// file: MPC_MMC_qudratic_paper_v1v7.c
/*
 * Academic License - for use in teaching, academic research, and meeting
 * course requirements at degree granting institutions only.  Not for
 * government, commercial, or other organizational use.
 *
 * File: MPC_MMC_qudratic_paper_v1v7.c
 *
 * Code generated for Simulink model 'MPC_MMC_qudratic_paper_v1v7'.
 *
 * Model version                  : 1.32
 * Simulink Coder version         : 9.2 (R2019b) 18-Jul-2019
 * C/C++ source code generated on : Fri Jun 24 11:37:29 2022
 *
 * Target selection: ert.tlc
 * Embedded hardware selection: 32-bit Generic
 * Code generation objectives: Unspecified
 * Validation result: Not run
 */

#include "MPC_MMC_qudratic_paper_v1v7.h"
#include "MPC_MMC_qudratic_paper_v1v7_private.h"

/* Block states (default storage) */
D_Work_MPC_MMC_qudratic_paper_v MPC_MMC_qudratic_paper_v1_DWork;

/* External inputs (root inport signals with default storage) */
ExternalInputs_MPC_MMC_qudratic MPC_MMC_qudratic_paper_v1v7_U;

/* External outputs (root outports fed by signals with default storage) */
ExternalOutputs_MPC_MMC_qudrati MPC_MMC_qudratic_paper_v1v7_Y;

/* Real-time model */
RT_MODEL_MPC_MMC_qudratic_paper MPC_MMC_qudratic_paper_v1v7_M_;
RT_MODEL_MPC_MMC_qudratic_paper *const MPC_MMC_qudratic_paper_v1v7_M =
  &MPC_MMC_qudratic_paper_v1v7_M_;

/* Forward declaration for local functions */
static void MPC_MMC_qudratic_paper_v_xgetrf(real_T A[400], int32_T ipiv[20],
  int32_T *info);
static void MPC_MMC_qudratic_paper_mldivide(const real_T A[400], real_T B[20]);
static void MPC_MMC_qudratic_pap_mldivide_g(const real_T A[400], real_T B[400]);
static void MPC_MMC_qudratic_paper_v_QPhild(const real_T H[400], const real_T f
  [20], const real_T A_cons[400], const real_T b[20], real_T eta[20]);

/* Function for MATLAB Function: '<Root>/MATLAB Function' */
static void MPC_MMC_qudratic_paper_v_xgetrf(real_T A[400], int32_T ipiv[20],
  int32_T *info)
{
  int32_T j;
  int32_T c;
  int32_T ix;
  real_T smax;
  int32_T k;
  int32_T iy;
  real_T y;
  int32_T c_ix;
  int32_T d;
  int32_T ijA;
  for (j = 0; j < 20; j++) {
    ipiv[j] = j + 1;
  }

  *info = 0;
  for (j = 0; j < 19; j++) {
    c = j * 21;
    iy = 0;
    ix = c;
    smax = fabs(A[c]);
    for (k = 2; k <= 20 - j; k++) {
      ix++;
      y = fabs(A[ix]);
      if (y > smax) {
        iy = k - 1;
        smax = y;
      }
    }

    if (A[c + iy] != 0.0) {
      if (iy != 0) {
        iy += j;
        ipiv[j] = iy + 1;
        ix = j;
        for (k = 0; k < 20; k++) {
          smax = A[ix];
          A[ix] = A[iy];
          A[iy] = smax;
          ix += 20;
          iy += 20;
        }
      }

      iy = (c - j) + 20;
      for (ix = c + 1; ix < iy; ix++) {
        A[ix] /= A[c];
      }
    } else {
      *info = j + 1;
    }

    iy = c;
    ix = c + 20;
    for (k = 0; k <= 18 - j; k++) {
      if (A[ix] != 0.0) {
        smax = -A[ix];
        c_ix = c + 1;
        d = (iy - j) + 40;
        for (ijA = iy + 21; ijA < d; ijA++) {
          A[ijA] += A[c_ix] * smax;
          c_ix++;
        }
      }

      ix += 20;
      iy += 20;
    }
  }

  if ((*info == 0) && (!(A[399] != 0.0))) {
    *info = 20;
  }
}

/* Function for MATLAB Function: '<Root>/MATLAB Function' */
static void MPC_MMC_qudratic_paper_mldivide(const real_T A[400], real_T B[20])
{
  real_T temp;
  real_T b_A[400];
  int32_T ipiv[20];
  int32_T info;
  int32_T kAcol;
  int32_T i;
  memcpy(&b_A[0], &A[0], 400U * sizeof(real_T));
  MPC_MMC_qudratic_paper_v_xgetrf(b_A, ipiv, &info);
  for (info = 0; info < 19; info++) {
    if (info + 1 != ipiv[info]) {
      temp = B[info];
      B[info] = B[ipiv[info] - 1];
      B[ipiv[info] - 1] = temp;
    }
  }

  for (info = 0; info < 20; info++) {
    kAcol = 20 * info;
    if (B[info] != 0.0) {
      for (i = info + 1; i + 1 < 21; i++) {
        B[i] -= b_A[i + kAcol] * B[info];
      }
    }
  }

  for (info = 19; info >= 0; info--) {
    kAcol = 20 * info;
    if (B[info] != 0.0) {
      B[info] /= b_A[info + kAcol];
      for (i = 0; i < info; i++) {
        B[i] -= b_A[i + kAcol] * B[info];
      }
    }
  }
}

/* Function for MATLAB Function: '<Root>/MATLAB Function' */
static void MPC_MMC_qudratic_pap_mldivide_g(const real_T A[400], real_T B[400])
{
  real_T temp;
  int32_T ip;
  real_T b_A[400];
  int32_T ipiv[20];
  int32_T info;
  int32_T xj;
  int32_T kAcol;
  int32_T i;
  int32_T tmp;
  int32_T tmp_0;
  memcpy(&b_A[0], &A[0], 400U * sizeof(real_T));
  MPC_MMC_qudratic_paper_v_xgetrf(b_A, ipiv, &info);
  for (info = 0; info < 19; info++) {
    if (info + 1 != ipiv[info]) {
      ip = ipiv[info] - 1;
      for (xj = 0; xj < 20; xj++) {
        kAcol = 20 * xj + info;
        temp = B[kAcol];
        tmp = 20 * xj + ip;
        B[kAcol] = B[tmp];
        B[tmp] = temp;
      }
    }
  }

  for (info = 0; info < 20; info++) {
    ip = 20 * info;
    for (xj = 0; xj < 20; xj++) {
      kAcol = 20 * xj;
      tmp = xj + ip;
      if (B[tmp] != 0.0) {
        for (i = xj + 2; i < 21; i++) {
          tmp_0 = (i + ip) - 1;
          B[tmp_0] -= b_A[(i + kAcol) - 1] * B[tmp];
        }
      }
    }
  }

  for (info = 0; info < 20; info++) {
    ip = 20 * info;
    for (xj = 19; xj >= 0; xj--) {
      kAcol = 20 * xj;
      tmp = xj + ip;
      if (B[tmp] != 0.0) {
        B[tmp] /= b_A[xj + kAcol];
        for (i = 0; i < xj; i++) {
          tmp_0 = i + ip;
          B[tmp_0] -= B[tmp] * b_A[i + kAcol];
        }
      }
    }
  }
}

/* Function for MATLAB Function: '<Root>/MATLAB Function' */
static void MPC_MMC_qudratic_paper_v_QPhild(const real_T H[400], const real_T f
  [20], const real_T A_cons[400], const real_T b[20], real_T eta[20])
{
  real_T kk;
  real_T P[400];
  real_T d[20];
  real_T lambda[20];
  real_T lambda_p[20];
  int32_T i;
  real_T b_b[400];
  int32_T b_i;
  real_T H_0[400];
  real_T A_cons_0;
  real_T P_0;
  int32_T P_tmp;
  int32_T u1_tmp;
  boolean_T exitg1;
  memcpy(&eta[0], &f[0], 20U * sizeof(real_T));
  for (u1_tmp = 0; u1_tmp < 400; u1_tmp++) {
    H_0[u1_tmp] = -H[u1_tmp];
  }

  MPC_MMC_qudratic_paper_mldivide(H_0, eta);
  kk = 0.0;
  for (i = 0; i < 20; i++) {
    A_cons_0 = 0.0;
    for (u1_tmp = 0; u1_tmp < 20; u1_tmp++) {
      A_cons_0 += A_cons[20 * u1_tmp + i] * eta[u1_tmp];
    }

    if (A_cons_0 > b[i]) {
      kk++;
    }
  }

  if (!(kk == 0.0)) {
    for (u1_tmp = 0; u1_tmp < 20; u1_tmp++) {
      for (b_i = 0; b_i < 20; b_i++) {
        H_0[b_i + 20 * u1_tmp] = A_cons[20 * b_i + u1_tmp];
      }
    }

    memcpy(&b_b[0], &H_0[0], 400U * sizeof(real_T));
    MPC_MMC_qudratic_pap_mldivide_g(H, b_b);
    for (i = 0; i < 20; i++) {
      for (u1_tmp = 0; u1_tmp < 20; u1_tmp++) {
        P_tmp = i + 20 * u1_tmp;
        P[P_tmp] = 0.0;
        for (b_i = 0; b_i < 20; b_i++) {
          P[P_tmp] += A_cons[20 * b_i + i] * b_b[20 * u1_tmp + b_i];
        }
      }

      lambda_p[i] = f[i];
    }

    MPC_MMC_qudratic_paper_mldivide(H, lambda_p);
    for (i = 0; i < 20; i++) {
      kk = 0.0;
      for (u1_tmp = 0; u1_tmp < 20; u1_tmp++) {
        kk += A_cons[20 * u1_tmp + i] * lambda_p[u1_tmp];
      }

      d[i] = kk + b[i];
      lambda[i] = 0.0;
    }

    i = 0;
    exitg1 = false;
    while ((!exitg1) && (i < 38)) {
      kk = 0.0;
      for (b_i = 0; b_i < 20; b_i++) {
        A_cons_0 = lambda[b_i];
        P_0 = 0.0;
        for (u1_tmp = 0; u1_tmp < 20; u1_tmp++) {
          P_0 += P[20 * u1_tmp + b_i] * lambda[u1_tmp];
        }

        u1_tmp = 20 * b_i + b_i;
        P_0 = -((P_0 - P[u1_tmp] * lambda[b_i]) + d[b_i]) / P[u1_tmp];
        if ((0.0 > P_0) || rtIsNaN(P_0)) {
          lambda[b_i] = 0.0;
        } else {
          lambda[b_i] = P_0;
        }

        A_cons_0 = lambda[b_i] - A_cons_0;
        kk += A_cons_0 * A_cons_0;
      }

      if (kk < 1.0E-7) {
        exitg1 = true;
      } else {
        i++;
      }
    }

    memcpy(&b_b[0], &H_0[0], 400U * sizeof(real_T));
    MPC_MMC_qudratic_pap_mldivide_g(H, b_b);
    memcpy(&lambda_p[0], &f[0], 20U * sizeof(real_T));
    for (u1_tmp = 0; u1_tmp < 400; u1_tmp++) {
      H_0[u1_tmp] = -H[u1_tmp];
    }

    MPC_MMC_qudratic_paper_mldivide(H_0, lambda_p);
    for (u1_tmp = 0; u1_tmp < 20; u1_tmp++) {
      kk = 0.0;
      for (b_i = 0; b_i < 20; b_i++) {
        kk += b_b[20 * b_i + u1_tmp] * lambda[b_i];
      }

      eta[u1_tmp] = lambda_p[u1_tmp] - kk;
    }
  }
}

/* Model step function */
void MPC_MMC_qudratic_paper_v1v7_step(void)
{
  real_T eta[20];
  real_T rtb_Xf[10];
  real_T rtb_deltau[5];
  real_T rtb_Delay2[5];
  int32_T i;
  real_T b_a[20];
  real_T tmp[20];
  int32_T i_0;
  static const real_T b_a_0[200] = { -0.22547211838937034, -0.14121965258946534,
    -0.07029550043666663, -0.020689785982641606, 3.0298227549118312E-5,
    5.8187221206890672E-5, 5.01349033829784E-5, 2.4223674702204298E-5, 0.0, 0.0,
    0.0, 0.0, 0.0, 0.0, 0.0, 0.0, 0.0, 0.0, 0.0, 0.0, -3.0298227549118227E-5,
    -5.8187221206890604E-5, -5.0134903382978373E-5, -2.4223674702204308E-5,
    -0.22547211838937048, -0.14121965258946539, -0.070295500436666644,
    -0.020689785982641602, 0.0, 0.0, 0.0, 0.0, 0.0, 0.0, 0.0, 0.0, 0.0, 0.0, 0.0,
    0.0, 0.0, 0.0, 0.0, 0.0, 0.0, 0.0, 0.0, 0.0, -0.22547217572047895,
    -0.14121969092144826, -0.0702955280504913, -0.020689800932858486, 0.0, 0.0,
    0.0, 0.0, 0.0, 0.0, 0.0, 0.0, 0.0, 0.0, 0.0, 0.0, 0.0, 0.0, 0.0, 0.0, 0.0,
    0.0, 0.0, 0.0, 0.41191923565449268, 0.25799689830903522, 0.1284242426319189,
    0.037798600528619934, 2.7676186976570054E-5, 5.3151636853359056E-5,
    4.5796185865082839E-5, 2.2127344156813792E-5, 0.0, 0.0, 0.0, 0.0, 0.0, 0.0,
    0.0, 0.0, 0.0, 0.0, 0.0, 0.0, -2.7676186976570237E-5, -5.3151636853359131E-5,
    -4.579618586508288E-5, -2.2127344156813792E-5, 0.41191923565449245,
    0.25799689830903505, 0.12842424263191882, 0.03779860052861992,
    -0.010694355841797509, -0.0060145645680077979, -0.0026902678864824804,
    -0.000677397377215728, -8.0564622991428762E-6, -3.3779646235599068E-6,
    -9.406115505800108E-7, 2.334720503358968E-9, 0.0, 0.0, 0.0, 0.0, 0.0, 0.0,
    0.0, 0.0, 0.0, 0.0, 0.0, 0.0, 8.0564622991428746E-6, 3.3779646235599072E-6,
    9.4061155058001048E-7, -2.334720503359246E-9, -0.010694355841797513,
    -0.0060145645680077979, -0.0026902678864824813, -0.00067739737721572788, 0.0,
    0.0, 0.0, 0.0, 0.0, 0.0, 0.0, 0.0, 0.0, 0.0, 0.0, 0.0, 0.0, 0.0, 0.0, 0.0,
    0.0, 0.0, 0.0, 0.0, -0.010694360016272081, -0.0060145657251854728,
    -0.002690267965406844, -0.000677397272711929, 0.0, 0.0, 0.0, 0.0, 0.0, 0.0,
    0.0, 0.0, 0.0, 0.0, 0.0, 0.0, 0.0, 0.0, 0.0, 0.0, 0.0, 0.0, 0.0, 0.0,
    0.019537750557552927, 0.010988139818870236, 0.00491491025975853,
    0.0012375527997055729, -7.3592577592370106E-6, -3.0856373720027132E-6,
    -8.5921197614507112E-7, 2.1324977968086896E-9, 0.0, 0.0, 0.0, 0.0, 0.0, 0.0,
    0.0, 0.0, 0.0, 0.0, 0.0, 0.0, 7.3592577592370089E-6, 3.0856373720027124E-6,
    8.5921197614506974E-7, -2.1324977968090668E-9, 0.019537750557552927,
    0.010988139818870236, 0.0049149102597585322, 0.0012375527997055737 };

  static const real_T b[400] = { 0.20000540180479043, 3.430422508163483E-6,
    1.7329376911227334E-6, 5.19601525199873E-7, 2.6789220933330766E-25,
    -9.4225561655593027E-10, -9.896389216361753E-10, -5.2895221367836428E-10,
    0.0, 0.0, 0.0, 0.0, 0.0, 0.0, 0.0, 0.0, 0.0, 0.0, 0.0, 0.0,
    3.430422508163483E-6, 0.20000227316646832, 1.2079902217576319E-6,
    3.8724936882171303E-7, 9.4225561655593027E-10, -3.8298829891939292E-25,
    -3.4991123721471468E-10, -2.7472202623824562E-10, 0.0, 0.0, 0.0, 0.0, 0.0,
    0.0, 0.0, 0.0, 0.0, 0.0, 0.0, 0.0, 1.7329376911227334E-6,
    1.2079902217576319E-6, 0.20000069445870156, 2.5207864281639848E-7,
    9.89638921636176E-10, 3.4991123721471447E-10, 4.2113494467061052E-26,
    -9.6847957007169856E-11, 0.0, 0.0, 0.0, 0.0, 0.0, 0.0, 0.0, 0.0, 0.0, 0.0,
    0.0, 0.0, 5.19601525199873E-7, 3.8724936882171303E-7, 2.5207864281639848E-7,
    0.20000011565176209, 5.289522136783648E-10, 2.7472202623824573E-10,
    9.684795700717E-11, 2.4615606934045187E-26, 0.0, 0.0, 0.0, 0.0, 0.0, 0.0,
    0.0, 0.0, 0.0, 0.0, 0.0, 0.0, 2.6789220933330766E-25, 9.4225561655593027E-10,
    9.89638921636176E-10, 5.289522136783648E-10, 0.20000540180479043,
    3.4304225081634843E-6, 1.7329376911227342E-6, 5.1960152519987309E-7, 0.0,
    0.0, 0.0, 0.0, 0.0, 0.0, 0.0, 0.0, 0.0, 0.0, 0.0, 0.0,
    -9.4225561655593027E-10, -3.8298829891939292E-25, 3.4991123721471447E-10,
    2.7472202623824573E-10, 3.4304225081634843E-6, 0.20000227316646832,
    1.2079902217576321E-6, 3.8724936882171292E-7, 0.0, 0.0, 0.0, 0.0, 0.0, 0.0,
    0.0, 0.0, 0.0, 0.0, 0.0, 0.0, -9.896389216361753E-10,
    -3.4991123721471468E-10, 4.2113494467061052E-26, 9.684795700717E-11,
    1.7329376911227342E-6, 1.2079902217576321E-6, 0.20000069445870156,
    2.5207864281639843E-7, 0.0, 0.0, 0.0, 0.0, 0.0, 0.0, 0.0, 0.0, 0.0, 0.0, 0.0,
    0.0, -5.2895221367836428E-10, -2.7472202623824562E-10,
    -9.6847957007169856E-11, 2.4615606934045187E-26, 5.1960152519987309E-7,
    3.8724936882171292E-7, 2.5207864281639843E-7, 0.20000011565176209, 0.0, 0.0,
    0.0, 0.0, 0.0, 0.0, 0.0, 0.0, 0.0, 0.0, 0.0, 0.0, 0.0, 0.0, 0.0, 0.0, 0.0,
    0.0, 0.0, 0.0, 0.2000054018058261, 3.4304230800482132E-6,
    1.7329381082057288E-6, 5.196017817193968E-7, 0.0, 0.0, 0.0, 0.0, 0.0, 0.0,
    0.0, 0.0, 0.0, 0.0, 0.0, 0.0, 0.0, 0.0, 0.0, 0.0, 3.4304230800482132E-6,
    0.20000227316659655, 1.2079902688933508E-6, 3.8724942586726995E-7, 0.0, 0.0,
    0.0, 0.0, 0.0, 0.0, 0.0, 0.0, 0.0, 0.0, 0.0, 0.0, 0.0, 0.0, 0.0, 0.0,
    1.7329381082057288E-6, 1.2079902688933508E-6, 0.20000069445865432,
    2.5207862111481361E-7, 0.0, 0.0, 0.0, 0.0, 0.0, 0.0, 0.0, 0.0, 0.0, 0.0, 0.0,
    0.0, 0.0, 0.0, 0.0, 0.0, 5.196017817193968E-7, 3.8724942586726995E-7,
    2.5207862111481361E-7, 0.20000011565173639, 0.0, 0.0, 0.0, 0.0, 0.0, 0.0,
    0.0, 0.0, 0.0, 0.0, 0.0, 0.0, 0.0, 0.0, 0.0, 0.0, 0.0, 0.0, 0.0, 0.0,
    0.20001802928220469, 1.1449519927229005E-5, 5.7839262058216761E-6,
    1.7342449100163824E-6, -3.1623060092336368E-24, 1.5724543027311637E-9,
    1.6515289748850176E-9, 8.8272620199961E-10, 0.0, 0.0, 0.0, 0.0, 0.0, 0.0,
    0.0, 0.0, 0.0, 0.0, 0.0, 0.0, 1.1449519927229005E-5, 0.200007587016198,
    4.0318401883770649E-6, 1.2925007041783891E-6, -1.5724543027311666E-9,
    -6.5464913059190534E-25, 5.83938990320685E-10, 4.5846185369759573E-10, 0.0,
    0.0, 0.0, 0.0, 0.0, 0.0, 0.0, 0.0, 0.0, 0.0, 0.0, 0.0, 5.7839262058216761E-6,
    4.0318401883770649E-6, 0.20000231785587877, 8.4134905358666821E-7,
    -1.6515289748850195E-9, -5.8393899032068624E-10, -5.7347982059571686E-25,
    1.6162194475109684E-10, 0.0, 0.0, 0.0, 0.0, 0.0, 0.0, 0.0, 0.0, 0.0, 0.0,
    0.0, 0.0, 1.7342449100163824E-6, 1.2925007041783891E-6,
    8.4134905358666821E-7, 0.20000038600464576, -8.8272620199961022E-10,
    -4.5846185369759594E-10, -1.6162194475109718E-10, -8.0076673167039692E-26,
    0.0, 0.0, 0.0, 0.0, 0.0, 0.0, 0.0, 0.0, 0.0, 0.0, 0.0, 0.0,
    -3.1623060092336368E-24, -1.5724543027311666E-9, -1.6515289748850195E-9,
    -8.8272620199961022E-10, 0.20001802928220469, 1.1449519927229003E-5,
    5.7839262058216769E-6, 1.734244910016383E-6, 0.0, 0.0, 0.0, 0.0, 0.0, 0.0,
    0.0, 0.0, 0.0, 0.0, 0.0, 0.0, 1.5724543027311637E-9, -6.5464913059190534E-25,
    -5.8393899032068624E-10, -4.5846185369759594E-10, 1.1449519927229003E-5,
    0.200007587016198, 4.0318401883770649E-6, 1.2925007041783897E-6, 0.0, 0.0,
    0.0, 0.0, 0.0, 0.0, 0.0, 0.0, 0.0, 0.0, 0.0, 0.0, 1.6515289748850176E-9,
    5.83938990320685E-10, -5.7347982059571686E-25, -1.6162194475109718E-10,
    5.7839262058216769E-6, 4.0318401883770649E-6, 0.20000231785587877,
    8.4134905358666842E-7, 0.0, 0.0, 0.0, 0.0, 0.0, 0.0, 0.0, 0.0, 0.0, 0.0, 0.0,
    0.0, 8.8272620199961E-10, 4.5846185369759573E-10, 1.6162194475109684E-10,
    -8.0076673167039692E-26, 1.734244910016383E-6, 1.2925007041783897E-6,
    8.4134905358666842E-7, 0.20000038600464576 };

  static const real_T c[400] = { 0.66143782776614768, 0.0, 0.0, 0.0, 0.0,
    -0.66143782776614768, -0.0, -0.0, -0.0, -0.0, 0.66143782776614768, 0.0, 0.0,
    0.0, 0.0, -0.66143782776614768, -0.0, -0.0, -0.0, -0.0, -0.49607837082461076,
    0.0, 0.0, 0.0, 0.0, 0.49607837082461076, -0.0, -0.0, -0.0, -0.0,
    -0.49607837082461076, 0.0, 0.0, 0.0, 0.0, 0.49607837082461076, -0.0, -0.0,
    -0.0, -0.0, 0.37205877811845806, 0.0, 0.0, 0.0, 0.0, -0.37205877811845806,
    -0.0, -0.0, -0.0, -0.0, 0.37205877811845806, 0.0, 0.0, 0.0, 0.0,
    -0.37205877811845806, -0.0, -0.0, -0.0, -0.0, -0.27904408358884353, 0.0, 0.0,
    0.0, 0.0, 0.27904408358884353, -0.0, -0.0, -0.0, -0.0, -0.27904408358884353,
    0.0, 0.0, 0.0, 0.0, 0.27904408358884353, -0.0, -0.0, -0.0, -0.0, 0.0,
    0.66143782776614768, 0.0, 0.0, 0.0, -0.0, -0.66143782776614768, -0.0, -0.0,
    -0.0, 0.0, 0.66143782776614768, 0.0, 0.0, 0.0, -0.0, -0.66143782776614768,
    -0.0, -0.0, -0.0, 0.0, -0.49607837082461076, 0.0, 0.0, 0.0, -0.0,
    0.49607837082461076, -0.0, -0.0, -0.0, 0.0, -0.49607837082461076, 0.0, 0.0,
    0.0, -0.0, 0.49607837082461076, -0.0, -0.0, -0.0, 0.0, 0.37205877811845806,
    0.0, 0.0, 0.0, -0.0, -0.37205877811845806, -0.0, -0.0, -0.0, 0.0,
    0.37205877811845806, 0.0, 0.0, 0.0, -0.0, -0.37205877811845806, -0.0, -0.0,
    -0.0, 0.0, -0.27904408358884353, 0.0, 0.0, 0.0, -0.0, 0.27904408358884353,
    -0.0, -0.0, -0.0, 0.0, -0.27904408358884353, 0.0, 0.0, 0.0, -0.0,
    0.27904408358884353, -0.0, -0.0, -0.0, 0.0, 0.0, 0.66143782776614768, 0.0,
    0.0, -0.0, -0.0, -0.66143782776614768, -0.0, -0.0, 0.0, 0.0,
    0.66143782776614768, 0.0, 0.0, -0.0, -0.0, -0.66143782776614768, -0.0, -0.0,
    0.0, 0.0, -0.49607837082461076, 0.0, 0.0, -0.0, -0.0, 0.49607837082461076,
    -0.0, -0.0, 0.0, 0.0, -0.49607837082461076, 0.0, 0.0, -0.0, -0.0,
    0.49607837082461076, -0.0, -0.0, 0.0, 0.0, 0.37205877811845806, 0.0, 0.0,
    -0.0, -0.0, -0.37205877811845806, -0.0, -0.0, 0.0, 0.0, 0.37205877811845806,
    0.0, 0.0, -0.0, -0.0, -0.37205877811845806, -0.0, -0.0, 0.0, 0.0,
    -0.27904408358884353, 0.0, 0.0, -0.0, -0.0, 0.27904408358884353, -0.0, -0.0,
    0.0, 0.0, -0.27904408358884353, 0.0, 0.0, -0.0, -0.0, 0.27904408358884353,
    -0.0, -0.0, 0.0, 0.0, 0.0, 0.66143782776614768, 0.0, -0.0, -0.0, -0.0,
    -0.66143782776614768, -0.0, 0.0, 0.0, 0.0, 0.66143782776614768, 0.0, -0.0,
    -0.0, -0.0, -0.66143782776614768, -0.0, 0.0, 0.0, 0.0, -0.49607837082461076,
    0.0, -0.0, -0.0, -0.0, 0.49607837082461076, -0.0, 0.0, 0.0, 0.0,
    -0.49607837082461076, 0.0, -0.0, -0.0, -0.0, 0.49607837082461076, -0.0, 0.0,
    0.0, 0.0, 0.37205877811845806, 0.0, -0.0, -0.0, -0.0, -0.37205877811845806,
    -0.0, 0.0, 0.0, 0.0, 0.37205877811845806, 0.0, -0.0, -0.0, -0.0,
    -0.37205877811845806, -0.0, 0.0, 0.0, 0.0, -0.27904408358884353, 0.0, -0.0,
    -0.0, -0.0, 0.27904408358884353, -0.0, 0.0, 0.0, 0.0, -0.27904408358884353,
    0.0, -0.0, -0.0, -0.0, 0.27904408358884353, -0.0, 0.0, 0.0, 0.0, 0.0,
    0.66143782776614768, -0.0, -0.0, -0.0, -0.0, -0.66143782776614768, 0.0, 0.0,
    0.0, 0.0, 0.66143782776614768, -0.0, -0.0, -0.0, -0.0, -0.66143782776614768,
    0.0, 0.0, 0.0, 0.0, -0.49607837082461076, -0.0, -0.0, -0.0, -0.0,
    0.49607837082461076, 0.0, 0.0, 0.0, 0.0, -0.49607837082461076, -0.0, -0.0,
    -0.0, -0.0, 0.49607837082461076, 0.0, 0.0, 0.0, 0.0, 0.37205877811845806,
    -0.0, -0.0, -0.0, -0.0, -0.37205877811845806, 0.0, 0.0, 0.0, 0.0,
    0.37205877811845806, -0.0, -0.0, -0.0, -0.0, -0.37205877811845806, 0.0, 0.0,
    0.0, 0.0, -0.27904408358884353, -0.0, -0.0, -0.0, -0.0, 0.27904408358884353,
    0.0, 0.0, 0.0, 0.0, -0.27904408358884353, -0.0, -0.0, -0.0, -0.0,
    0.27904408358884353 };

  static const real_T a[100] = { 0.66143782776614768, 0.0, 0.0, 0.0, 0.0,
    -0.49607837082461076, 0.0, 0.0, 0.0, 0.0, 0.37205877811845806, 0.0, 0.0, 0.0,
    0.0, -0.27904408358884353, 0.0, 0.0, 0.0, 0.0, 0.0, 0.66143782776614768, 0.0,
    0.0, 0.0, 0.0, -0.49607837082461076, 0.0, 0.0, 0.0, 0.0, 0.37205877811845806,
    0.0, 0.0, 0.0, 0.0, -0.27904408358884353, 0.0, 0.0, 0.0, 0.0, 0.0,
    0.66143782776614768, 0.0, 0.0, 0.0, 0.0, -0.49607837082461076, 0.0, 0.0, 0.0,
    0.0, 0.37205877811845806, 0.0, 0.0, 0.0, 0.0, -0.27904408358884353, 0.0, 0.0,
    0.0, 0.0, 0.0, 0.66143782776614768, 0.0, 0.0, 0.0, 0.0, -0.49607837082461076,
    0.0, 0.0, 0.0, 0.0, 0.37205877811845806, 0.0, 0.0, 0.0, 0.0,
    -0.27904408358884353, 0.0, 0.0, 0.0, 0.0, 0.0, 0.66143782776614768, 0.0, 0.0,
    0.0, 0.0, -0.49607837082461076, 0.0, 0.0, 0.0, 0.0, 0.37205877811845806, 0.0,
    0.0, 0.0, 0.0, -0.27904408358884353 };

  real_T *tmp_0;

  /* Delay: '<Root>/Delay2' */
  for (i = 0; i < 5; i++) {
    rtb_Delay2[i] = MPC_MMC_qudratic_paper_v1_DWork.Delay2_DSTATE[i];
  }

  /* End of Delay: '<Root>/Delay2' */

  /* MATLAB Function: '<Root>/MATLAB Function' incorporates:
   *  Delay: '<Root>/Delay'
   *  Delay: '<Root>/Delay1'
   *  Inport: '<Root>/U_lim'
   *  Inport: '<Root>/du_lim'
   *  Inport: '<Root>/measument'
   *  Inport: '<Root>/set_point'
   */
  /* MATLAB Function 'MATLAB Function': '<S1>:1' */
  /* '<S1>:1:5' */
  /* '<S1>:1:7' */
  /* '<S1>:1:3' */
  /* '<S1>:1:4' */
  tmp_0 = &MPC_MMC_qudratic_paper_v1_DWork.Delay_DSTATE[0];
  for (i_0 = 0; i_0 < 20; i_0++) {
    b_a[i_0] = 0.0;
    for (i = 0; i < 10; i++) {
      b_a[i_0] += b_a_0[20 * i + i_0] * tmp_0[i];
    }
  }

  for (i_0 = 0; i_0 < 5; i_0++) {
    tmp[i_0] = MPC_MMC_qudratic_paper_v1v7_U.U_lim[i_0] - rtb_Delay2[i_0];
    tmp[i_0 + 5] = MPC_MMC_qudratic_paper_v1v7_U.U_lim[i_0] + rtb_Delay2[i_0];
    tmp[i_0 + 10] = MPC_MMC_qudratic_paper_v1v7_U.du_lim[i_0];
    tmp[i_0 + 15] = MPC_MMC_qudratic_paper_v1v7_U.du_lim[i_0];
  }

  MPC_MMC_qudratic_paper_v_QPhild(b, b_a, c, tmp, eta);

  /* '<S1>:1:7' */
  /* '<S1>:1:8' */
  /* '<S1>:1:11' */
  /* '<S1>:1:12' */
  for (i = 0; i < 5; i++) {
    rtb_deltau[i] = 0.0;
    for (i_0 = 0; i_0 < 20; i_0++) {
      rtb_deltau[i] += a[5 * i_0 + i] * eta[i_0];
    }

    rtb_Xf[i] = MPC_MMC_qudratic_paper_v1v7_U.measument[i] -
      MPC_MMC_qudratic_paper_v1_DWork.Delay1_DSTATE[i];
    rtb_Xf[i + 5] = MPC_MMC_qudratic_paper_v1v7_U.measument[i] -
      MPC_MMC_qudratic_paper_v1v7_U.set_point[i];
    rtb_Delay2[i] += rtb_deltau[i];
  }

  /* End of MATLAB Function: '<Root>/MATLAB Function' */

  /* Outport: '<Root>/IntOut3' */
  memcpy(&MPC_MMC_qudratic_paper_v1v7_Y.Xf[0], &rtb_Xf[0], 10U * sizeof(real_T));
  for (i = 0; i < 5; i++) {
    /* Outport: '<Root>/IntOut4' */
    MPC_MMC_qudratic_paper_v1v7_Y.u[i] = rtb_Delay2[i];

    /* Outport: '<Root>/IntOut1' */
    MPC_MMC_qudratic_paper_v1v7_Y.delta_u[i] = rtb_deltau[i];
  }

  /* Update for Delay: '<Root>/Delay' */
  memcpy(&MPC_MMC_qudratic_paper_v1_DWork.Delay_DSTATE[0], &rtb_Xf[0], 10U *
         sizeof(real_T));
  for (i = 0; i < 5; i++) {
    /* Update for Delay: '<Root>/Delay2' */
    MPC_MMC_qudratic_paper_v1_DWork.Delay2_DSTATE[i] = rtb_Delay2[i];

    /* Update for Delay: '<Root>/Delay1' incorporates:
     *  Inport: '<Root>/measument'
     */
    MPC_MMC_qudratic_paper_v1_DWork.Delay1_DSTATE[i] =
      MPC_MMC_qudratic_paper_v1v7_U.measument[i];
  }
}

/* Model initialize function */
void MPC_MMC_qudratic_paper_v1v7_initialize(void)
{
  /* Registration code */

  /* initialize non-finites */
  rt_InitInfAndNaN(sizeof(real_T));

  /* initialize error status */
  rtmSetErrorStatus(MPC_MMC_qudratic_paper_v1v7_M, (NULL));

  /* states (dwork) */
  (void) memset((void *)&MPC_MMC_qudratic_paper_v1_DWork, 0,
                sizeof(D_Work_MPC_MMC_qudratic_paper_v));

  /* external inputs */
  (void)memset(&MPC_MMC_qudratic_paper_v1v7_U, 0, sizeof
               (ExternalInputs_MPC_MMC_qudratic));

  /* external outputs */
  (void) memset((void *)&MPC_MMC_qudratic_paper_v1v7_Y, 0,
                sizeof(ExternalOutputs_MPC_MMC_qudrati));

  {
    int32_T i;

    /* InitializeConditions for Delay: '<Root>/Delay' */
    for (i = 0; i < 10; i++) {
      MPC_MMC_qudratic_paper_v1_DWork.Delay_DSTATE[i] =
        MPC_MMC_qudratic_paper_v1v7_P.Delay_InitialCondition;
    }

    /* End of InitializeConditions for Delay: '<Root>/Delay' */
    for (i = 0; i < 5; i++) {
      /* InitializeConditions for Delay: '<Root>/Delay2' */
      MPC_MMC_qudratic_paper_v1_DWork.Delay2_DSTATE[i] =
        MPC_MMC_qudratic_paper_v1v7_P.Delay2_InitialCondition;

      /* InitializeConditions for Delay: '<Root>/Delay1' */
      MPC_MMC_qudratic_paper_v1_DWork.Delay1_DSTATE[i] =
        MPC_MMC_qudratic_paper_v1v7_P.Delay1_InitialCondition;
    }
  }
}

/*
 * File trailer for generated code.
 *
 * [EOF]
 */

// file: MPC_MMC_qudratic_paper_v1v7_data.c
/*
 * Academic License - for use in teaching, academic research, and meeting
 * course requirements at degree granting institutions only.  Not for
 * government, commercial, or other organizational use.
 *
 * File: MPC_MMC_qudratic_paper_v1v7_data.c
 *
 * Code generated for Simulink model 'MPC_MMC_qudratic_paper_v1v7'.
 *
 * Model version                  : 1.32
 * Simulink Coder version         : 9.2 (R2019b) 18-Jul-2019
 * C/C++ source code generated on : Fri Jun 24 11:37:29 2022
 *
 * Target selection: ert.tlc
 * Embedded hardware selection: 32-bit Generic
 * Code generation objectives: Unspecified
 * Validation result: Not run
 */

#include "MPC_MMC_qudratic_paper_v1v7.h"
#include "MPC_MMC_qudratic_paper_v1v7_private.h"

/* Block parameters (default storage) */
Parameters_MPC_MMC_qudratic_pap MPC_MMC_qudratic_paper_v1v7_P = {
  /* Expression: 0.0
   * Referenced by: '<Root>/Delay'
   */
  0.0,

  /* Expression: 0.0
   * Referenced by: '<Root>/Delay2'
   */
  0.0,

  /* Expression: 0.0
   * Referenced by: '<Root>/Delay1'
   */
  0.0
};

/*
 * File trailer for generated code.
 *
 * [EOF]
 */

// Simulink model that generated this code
simulink model "MPC_MMC_qudratic_paper_v1v7"  (R2019b)
settings: Solver=ode3  StartTime=0.0  StopTime=3  FixedStep=0.000080  RelTol=1e-3  EnableMultiTasking=on

== system MPC_MMC_qudratic_paper_v1v7 ==
  set_point : Inport  PortDimensions=5
  measument : Inport  Port=2  PortDimensions=5
  U_lim : Inport  Port=3  PortDimensions=5
  du_lim : Inport  Port=4  PortDimensions=5
  Delay : Delay  DelayLength=1
  Delay1 : Delay  DelayLength=1
  Delay2 : Delay  DelayLength=1
  MATLAB Function : MATLAB Function  TreatAsAtomicUnit=on
  IntOut3 : Outport  SignalName=Xf
  IntOut4 : Outport  Port=2  SignalName=u
  IntOut1 : Outport  Port=3  SignalName=delta_u
  wires:
  set_point/1 -> MATLAB Function/1(r)
  MATLAB Function/1(Xf) -> Delay/1, IntOut3/1
  measument/1 -> MATLAB Function/2(xm_old), Delay1/1
  MATLAB Function/3(deltau) -> IntOut1/1
  Delay1/1 -> MATLAB Function/5(Xm_k_1)
  Delay/1 -> MATLAB Function/3(Xf_old)
  Delay2/1 -> MATLAB Function/4(u_old)
  MATLAB Function/2(u) -> Delay2/1, IntOut4/1
  U_lim/1 -> MATLAB Function/6(U_lim)
  du_lim/1 -> MATLAB Function/7(du_lim)

== matlab function MPC_MMC_qudratic_paper_v1v7/MATLAB Function ==
function [Xf,u,deltau] = fcn(r,xm_old,Xf_old,u_old,Xm_k_1,U_lim,du_lim)
D = []; 
D= coder.load('initial_qudratic_papervx.mat'); 
gamma=[(U_lim - u_old);(U_lim + u_old); du_lim; du_lim];
eta = QPhild(D.Omega,D.Psi*(D.Xf+Xf_old),D.M,gamma);
%eta= -(D.Omega\D.Psi)*(D.Xf+Xf_old);
deltau= D.Lzerot*eta;
u=D.up+u_old+deltau;
y = xm_old;
xm = xm_old;
y_delta_k=y-Xm_k_1;
Xf=[y_delta_k;y-r];
end
